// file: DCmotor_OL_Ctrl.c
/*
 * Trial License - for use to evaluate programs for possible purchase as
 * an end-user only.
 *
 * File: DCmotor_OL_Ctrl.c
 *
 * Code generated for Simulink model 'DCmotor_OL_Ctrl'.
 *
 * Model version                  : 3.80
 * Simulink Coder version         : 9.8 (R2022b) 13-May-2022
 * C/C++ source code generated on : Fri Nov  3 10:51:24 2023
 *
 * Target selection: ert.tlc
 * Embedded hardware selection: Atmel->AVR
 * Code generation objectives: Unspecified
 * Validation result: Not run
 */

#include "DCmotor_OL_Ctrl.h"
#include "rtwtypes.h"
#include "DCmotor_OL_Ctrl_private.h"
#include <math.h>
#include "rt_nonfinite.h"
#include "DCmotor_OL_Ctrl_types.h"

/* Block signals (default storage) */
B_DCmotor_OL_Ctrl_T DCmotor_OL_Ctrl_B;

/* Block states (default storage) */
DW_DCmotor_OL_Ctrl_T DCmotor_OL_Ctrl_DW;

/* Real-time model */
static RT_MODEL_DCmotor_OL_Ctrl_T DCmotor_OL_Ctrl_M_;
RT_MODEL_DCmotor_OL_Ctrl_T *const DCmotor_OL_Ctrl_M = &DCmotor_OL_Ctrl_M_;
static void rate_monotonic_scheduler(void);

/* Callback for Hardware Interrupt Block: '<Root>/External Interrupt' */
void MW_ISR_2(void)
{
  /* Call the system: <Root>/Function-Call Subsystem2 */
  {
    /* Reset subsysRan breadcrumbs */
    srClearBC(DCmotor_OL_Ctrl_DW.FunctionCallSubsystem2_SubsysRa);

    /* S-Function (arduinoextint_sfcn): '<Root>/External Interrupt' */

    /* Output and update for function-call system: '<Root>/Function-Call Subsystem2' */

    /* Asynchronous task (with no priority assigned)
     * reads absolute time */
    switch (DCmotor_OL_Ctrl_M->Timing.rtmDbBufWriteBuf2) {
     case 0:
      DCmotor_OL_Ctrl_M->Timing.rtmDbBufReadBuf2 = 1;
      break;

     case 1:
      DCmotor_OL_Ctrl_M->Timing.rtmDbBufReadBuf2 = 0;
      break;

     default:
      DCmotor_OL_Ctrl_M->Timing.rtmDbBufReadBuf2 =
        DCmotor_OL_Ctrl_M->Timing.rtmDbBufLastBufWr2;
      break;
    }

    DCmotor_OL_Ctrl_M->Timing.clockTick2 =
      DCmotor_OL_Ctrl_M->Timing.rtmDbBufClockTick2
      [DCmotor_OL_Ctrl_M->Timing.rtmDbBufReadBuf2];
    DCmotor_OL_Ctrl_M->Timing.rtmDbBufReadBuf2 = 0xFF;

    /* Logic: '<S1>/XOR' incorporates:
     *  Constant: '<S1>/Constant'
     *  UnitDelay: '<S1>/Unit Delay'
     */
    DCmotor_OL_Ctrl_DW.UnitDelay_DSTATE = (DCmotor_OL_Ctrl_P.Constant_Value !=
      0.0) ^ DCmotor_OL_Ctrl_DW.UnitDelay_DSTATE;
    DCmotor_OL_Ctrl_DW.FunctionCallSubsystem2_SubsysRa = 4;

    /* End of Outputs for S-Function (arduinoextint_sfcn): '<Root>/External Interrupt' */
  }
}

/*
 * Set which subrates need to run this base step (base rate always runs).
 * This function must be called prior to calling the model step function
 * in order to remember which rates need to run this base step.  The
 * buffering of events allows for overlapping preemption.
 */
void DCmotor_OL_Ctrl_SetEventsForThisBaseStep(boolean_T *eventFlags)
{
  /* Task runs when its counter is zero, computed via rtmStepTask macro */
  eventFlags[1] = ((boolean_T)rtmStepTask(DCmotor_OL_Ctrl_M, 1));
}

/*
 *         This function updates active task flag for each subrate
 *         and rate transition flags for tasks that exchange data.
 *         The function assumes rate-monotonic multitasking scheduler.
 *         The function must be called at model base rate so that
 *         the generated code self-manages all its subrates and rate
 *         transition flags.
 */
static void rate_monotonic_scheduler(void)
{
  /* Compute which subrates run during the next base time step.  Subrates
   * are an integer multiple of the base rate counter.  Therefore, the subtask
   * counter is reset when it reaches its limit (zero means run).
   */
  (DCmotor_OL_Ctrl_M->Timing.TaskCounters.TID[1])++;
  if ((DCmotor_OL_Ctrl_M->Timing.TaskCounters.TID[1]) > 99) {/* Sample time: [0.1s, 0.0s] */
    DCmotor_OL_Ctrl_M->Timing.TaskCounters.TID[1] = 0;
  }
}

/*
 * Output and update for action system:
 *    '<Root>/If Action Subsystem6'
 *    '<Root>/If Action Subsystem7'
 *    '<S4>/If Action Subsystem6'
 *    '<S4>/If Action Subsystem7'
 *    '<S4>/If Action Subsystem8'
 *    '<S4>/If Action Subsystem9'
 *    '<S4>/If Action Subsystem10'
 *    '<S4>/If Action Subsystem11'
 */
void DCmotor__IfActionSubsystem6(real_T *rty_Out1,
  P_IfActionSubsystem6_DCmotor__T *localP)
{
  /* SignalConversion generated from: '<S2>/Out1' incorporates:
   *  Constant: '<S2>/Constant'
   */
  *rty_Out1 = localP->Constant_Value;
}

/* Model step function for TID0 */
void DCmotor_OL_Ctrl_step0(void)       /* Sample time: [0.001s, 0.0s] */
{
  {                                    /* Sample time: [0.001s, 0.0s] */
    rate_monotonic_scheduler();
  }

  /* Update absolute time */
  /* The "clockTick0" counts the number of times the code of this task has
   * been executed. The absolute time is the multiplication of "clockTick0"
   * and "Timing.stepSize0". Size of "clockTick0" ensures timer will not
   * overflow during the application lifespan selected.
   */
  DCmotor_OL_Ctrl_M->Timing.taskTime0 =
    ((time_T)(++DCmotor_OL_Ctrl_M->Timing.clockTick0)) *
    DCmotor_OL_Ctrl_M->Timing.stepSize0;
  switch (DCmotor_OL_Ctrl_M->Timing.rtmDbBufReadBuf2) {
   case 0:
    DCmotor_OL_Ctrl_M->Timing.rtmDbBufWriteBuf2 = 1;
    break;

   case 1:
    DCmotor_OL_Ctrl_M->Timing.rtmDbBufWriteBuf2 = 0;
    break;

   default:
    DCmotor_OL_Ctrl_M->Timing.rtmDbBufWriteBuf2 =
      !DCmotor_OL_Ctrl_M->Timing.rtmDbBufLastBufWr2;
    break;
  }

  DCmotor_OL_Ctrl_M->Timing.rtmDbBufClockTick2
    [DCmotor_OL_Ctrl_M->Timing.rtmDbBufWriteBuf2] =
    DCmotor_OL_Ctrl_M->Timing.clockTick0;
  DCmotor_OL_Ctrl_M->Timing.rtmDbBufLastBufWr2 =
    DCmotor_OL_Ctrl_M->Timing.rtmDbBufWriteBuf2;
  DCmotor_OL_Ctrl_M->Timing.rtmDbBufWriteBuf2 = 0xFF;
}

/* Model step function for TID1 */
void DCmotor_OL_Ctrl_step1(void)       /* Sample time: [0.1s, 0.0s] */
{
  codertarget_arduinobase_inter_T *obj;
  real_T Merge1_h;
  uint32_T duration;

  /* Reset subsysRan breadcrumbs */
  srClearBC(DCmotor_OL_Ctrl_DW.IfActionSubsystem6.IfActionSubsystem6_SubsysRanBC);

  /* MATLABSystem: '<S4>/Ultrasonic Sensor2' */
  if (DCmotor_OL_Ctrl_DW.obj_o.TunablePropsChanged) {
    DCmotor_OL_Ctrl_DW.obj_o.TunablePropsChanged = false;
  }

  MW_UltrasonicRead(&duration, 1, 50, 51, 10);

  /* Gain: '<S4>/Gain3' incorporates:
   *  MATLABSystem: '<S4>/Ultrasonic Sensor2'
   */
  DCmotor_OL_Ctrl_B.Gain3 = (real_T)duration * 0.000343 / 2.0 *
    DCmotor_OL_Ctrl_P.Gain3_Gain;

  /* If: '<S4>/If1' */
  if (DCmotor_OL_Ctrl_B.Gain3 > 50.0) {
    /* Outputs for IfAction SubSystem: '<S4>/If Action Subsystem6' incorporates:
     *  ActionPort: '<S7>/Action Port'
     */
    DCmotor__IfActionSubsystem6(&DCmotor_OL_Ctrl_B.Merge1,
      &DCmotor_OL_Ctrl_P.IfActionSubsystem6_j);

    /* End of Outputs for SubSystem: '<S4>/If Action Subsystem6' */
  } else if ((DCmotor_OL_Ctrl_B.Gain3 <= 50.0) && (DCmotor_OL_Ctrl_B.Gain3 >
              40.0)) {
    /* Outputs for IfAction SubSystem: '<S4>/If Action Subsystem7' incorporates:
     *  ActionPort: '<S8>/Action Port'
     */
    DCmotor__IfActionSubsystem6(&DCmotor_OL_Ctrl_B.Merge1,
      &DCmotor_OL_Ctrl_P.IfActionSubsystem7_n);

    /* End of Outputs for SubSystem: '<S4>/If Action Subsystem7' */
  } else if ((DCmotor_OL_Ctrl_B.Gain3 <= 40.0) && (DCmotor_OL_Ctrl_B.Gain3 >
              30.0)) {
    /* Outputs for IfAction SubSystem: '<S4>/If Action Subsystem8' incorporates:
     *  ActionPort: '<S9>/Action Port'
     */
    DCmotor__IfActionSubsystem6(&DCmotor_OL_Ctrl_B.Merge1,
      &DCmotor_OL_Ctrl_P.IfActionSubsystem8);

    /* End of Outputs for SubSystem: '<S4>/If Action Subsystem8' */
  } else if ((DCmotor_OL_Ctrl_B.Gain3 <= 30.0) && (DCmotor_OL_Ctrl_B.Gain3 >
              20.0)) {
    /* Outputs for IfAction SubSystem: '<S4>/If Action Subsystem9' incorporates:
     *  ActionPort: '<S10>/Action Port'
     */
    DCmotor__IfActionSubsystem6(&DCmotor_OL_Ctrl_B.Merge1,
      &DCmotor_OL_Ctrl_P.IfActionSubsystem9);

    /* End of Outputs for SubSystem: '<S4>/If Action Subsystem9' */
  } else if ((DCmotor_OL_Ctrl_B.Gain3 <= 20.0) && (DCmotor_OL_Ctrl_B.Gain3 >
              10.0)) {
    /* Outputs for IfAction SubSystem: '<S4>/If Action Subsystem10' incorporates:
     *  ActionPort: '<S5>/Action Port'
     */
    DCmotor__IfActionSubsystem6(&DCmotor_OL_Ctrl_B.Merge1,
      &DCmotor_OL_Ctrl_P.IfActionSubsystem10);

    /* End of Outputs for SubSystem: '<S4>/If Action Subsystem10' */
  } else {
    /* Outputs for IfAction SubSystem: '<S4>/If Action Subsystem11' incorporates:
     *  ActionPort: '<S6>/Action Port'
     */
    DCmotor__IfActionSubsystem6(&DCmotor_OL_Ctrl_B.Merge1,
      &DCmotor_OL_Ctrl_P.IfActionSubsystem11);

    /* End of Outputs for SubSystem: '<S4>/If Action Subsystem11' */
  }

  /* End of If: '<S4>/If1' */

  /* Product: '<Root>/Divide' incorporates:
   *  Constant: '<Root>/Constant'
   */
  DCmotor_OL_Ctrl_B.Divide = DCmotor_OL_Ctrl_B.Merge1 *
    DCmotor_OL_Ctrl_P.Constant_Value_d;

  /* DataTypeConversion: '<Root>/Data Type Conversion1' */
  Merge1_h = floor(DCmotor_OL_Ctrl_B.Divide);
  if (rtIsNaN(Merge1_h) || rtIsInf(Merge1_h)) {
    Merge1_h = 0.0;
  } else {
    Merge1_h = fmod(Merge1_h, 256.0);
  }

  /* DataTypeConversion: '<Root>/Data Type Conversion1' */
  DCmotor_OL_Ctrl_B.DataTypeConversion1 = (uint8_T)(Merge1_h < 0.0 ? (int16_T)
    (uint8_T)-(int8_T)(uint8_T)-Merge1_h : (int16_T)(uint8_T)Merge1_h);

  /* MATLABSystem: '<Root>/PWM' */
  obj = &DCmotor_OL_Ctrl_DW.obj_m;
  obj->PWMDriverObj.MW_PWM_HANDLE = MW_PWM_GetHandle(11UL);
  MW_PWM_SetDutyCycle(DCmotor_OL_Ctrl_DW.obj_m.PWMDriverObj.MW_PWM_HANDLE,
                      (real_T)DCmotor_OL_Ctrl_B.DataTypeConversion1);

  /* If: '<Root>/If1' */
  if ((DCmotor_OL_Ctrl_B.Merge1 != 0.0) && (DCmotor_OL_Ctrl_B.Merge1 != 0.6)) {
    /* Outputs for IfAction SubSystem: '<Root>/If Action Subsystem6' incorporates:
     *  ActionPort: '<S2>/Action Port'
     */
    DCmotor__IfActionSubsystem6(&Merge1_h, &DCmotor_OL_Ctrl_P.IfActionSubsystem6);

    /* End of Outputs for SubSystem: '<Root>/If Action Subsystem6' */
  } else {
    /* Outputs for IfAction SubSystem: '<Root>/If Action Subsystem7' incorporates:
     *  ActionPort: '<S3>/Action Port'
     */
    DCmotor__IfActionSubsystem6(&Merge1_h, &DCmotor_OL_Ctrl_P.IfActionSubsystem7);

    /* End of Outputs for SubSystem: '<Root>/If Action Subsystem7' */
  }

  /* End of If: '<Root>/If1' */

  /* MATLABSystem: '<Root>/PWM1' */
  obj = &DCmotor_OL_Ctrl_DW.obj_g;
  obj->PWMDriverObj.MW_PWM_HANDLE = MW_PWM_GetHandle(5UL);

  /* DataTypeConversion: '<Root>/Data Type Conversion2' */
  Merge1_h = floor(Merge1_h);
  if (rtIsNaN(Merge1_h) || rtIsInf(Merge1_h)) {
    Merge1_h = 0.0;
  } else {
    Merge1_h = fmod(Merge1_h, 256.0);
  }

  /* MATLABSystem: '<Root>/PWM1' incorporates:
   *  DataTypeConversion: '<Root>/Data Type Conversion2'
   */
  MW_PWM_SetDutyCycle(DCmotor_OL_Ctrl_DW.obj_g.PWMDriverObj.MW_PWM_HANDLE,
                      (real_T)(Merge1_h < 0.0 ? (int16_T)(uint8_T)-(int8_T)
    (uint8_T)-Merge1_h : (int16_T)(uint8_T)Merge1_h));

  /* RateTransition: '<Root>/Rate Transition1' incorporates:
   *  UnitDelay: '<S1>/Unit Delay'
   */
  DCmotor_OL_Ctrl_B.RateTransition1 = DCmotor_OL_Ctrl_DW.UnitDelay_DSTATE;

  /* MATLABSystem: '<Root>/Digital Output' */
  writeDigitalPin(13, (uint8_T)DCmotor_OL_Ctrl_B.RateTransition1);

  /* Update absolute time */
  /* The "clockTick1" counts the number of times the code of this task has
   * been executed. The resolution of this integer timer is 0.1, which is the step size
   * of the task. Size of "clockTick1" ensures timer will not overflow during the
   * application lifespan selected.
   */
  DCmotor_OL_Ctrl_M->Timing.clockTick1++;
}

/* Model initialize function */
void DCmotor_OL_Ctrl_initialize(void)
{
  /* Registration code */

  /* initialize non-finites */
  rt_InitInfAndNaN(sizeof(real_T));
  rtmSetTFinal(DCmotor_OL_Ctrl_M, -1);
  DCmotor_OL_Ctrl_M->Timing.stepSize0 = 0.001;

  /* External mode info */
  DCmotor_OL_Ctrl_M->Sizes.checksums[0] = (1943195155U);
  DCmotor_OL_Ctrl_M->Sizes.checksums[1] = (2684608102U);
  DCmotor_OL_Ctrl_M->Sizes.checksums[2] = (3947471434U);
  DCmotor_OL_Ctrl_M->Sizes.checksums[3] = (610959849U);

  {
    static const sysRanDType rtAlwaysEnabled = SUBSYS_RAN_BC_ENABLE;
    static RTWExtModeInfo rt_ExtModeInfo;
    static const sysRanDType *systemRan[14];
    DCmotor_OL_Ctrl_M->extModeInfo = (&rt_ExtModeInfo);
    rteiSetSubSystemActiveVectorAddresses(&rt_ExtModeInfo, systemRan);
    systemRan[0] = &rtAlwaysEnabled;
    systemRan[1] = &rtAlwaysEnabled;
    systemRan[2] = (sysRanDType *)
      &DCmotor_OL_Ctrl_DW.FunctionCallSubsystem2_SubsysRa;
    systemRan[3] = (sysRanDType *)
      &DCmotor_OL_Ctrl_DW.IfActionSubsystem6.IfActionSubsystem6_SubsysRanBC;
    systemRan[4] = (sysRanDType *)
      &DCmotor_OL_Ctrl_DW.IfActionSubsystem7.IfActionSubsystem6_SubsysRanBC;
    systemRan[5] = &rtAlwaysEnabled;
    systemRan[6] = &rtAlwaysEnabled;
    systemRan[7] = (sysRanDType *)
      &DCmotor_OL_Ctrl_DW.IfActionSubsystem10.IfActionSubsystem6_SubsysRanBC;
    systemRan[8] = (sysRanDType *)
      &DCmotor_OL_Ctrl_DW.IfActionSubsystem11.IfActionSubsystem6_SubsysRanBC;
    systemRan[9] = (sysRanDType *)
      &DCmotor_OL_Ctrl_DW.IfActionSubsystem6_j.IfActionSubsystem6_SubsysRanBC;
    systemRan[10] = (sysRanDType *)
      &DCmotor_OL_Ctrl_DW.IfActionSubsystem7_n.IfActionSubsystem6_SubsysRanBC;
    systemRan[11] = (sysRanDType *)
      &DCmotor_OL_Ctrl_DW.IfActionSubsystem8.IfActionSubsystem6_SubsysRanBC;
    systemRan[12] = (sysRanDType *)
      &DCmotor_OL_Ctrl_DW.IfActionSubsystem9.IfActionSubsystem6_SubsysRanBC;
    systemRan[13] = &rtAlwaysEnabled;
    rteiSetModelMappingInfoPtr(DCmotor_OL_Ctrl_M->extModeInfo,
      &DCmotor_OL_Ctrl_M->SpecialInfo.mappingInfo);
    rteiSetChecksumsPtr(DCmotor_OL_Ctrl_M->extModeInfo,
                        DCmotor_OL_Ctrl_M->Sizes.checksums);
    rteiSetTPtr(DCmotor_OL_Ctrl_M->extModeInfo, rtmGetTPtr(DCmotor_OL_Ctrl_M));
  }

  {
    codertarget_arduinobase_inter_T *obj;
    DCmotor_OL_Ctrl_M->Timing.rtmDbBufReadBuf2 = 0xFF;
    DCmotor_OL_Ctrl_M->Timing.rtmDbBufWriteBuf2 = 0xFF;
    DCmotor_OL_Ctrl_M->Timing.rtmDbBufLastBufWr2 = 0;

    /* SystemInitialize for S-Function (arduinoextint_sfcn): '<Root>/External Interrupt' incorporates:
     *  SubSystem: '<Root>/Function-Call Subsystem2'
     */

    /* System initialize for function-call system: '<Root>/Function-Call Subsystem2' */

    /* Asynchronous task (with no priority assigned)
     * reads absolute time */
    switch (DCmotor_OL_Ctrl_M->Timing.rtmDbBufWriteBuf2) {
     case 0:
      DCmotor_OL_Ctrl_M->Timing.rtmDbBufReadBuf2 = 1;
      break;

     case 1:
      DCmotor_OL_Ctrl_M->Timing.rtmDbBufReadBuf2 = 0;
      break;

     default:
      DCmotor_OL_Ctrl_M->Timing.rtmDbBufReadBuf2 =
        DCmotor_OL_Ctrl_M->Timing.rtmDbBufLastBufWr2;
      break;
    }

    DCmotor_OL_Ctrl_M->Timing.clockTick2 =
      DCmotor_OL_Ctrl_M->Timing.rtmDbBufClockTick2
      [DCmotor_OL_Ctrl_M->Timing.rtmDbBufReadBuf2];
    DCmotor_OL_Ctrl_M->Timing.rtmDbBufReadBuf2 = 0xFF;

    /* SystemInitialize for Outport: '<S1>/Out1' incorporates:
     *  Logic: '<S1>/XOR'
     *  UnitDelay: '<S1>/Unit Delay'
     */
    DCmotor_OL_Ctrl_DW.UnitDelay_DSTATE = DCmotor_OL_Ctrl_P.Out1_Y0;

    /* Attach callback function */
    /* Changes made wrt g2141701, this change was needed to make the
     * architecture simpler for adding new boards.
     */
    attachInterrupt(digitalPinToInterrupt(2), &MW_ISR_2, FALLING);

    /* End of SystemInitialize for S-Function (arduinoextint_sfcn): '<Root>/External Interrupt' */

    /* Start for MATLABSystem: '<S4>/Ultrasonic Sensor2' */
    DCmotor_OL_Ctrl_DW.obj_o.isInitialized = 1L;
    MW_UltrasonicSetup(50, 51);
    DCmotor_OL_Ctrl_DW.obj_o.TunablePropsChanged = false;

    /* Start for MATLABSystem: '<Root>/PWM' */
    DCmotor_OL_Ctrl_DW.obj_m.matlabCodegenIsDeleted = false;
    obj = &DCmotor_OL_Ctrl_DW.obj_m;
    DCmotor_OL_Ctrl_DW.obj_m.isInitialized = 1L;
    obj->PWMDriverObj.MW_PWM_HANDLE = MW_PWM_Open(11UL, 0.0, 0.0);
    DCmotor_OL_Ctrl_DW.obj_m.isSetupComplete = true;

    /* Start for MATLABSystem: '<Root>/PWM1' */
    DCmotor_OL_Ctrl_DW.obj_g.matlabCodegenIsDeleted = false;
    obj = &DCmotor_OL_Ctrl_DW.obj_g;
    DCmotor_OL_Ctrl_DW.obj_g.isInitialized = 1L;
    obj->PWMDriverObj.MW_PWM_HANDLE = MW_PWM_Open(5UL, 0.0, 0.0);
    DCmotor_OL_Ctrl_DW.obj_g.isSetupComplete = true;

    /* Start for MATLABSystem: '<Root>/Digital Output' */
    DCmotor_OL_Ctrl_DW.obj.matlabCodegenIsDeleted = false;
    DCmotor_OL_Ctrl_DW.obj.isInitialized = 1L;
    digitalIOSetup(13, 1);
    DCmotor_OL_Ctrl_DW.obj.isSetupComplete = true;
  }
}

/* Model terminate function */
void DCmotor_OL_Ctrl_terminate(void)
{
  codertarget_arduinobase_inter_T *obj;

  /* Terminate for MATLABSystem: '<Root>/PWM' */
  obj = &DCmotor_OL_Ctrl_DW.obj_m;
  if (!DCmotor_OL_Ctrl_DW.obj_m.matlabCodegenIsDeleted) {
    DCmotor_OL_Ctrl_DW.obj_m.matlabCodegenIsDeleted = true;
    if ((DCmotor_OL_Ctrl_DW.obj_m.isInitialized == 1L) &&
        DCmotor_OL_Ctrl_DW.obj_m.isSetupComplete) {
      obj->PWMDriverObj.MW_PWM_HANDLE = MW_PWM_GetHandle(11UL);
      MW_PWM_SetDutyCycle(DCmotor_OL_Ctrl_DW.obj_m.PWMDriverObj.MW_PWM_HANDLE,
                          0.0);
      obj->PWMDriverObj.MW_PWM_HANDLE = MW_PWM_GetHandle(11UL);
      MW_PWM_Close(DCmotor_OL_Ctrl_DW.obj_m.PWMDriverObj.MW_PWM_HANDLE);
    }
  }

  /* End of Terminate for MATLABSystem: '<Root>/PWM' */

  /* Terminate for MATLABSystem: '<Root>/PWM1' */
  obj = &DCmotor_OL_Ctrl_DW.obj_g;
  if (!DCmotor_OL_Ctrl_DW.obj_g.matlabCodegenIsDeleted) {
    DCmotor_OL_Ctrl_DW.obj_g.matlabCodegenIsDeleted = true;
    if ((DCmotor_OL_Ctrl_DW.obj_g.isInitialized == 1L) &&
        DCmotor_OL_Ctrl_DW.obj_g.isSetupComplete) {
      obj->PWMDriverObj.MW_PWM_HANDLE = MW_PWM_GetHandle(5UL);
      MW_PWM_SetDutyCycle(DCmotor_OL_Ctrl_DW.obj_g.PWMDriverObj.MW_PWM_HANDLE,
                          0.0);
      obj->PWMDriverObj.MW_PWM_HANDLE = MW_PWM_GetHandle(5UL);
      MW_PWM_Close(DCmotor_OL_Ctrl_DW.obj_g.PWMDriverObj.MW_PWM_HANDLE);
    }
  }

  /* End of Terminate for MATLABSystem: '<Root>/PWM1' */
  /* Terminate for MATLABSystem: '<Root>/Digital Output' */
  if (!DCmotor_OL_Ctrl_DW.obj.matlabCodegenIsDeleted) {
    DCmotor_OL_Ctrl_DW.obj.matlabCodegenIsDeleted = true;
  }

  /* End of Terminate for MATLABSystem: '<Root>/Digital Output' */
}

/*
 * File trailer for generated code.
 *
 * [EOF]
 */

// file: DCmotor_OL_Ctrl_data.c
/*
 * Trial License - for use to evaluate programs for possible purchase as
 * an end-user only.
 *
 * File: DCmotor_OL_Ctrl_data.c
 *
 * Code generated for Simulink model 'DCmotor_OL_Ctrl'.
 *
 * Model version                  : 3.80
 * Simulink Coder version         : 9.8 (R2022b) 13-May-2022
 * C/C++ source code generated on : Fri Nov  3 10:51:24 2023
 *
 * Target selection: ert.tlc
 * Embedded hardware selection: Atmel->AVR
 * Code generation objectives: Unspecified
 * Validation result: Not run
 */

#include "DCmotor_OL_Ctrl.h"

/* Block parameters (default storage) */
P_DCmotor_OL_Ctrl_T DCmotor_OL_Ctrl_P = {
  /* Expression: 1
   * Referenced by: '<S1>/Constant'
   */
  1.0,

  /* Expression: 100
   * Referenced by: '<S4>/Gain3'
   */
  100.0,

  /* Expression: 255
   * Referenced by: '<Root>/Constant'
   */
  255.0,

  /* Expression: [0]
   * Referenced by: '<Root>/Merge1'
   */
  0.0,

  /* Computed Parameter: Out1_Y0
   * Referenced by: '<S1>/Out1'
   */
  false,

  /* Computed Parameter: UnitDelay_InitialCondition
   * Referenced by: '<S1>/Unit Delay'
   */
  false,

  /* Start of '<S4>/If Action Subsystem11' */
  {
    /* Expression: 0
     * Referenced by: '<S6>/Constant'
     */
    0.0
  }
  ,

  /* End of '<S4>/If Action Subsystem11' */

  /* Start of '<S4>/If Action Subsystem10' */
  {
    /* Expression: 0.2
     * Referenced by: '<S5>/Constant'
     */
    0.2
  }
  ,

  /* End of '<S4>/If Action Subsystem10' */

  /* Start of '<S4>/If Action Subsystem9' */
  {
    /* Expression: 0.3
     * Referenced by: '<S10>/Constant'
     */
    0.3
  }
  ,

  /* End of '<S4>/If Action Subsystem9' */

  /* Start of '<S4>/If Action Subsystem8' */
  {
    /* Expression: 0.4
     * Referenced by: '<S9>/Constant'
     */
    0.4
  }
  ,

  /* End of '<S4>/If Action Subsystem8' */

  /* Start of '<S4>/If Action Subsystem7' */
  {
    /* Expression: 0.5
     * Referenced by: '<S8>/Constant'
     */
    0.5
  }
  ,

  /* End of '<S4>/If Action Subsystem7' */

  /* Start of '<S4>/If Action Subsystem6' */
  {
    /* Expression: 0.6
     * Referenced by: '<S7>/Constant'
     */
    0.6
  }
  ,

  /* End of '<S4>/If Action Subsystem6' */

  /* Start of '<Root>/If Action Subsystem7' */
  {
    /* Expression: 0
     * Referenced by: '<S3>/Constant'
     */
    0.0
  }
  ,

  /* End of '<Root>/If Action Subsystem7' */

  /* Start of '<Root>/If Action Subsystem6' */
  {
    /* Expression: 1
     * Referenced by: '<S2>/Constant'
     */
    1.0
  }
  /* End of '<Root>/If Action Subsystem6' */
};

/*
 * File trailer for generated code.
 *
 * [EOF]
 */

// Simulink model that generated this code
simulink model "DCmotor_OL_Ctrl"  (R2022b)
settings: Solver=ode4  StartTime=0.0  StopTime=inf  FixedStep=0.001  RelTol=1e-3  EnableMultiTasking=on
libraries: arduinolib x5, arduinosensorlib x2

== system DCmotor_OL_Ctrl ==
  note: Speed Control
  note: Ultra Sensor
  note: Direction Control
  Analog Input : arduinolib/Analog Input  Commented=on  pinNumber=0  ReadResultsOnly=off  ConversionTriggerSource=Software  ExternalTriggerType=uint32( 0 )  OutputDataType=uint16  EnableConversionCompleteNotify=off  EnableOuputStatus=off  SampleTime=-1  blockPlatform=arduino
  Constant : Constant  Value=255
  Data Type Conversion : DataTypeConversion  Commented=on  OutDataTypeStr=uint8  SaturateOnIntegerOverflow=off  RndMeth=Floor
  Data Type Conversion1 : DataTypeConversion  OutDataTypeStr=uint8  SaturateOnIntegerOverflow=off  RndMeth=Floor
  Data Type Conversion2 : DataTypeConversion  OutDataTypeStr=uint8  SaturateOnIntegerOverflow=off  RndMeth=Floor
  Digital Output : arduinolib/Digital Output  Commented=on  pinNumber=13  Direction=output  blockPlatform=arduino
  Display Status1 : Display  Commented=on
  Display1 : Display
  Display2 : Display
  Display3 : Display  Commented=on
  Divide : Product  Inputs=**
  External Interrupt : arduinolib/External Interrupt  Commented=on  Pin=2  PullUp=off  Mode=FALLING  InterruptSimulationInput=off
  Function-Call Subsystem : Subsystem  Commented=on  TreatAsAtomicUnit=on
  Function-Call Subsystem2 : Subsystem  Commented=on  TreatAsAtomicUnit=on
  Gain1 : Gain  Commented=on  Gain=0.25
  Gain2 : Gain  Commented=on  Gain=100
  If : If  Commented=on  IfExpression=u1 > 50  ElseIfExpressions=u1 > 40, u1 > 30, u1 > 20, u1 > 10
  If Action Subsystem : Subsystem  Commented=on  TreatAsAtomicUnit=on
  If Action Subsystem1 : Subsystem  Commented=on  TreatAsAtomicUnit=on
  If Action Subsystem2 : Subsystem  Commented=on  TreatAsAtomicUnit=on
  If Action Subsystem3 : Subsystem  Commented=on  TreatAsAtomicUnit=on
  If Action Subsystem4 : Subsystem  Commented=on  TreatAsAtomicUnit=on
  If Action Subsystem5 : Subsystem  Commented=on  TreatAsAtomicUnit=on
  If Action Subsystem6 : Subsystem  TreatAsAtomicUnit=on
  If Action Subsystem7 : Subsystem  TreatAsAtomicUnit=on
  If1 : If  IfExpression=u1 ~= 0 & u1 ~= 0.6
  Merge : Merge  Commented=on  Inputs=6
  Merge1 : Merge  InitialOutput=[0]
  PWM : arduinolib/PWM  pinNumber=11  frequencyType=Default  desiredFrequency=490.2  achievableFrequency=490.2
  PWM1 : arduinolib/PWM  pinNumber=5  frequencyType=Default  desiredFrequency=490.2  achievableFrequency=490.2
  Rate Transition1 : RateTransition  Commented=on  Deterministic=off
  Subsystem : Subsystem
  Ultrasonic Sensor1 : arduinosensorlib/Ultrasonic Sensor  Commented=on  NumSignalPins=2  TrigPin=50  EchoPin=51  SignalPin=3  SampleTime_=0.1  blockPlatform=ARDUINO
  Scope : Scope
  wires:
  Analog Input/1 -> Gain1/1
  Gain1/1 -> Data Type Conversion/1
  Constant/1 -> Divide/2
  Data Type Conversion1/1 -> PWM/1, Display2/1
  Gain2/1 -> Display3/1, If/1
  Ultrasonic Sensor1/1 -> Gain2/1
  If/2 -> If Action Subsystem1/Action
  If/1 -> If Action Subsystem/Action
  If/3 -> If Action Subsystem2/Action
  If/4 -> If Action Subsystem3/Action
  If/5 -> If Action Subsystem4/Action
  If/6 -> If Action Subsystem5/Action
  If Action Subsystem/1(Out1) -> Merge/1
  If Action Subsystem1/1(Out1) -> Merge/2
  If Action Subsystem2/1(Out1) -> Merge/3
  If Action Subsystem3/1(Out1) -> Merge/4
  If Action Subsystem4/1(Out1) -> Merge/5
  If Action Subsystem5/1(Out1) -> Merge/6
  Divide/1 -> Display1/1, Data Type Conversion1/1
  Function-Call Subsystem2/1(Out1) -> Rate Transition1/1
  Rate Transition1/1 -> Display Status1/1, Digital Output/1
  External Interrupt/1 -> Function-Call Subsystem2/Trigger
  Subsystem/1(Output) -> Divide/1, If1/1
  Data Type Conversion2/1 -> PWM1/1
  If Action Subsystem6/1(Out1) -> Merge1/1
  If Action Subsystem7/1(Out1) -> Merge1/2
  If1/1 -> If Action Subsystem6/Action
  If1/2 -> If Action Subsystem7/Action
  Merge1/1 -> Data Type Conversion2/1

== system DCmotor_OL_Ctrl/Function-Call Subsystem ==
  function : TriggerPort  TriggerType=function-call  VariantControl=(inherit)
  Constant : Constant
  MATLAB Function : MATLAB Function  TreatAsAtomicUnit=on
  Sum : Sum  Inputs=|++
  Unit Delay : UnitDelay  SampleTime=-1  HasFrameUpgradeWarning=on
  Out1 : Outport
  wires:
  Constant/1 -> Sum/1
  Unit Delay/1 -> Sum/2
  Sum/1 -> Unit Delay/1, MATLAB Function/1(u)
  MATLAB Function/1(y) -> Out1/1

== system DCmotor_OL_Ctrl/Function-Call Subsystem2 ==
  function : TriggerPort  TriggerType=function-call  VariantControl=(inherit)
  Constant : Constant
  Unit Delay : UnitDelay  SampleTime=-1  HasFrameUpgradeWarning=on
  XOR : Logic  Operator=XOR  IconShape=distinctive  AllPortsSameDT=off  OutDataTypeStr=boolean
  Out1 : Outport
  wires:
  Constant/1 -> XOR/1
  Unit Delay/1 -> XOR/2
  XOR/1 -> Unit Delay/1, Out1/1

== system DCmotor_OL_Ctrl/If Action Subsystem ==
  Action Port : ActionPort  ActionPortLabel=if(u1 > 50)
  Constant : Constant
  Out1 : Outport
  wires:
  Constant/1 -> Out1/1

== system DCmotor_OL_Ctrl/If Action Subsystem1 ==
  Action Port : ActionPort  ActionPortLabel=elseif(u1 > 40)
  Constant : Constant  Value=10
  Out1 : Outport
  wires:
  Constant/1 -> Out1/1

== system DCmotor_OL_Ctrl/If Action Subsystem2 ==
  Action Port : ActionPort  ActionPortLabel=elseif( u1 > 30)
  Constant : Constant  Value=10
  Out1 : Outport
  wires:
  Constant/1 -> Out1/1

== system DCmotor_OL_Ctrl/If Action Subsystem3 ==
  Action Port : ActionPort  ActionPortLabel=elseif( u1 > 20)
  Constant : Constant  Value=10
  Out1 : Outport
  wires:
  Constant/1 -> Out1/1

== system DCmotor_OL_Ctrl/If Action Subsystem4 ==
  Action Port : ActionPort  ActionPortLabel=elseif( u1 > 10)
  Constant : Constant  Value=10
  Out1 : Outport
  wires:
  Constant/1 -> Out1/1

== system DCmotor_OL_Ctrl/If Action Subsystem5 ==
  Action Port : ActionPort  ActionPortLabel=else
  Constant : Constant  Value=0
  Out1 : Outport
  wires:
  Constant/1 -> Out1/1

== system DCmotor_OL_Ctrl/If Action Subsystem6 ==
  Action Port : ActionPort  ActionPortLabel=if(u1 ~= 0 & u1 ~= 0.6)
  Constant : Constant  Value=10
  Out1 : Outport
  wires:
  Constant/1 -> Out1/1

== system DCmotor_OL_Ctrl/If Action Subsystem7 ==
  Action Port : ActionPort  ActionPortLabel=else
  Constant : Constant  Value=0
  Out1 : Outport
  wires:
  Constant/1 -> Out1/1

== system DCmotor_OL_Ctrl/Subsystem ==
  note: Ultra Sensor
  Display1 : Display
  Display4 : Display
  Gain3 : Gain  Gain=100
  If Action Subsystem10 : Subsystem  TreatAsAtomicUnit=on
  If Action Subsystem11 : Subsystem  TreatAsAtomicUnit=on
  If Action Subsystem6 : Subsystem  TreatAsAtomicUnit=on
  If Action Subsystem7 : Subsystem  TreatAsAtomicUnit=on
  If Action Subsystem8 : Subsystem  TreatAsAtomicUnit=on
  If Action Subsystem9 : Subsystem  TreatAsAtomicUnit=on
  If1 : If  IfExpression=u1 > 50  ElseIfExpressions=50>= u1 & u1> 40, 40>=u1 & u1>30, 30>= u1 & u1 > 20, 20>= u1 & u1 > 10
  Merge1 : Merge  Inputs=6
  Ultrasonic Sensor2 : arduinosensorlib/Ultrasonic Sensor  NumSignalPins=2  TrigPin=50  EchoPin=51  SignalPin=3  SampleTime_=0.1  blockPlatform=ARDUINO
  Output : Outport
  wires:
  Gain3/1 -> If1/1, Display4/1
  Ultrasonic Sensor2/1 -> Gain3/1
  If Action Subsystem9/1(Out1) -> Merge1/4
  If Action Subsystem11/1(Out1) -> Merge1/6
  If Action Subsystem8/1(Out1) -> Merge1/3
  If Action Subsystem7/1(Out1) -> Merge1/2
  If Action Subsystem6/1(Out1) -> Merge1/1
  If Action Subsystem10/1(Out1) -> Merge1/5
  If1/1 -> If Action Subsystem6/Action
  If1/2 -> If Action Subsystem7/Action
  If1/3 -> If Action Subsystem8/Action
  If1/4 -> If Action Subsystem9/Action
  If1/5 -> If Action Subsystem10/Action
  If1/6 -> If Action Subsystem11/Action
  Merge1/1 -> Display1/1, Output/1

== system DCmotor_OL_Ctrl/Subsystem/If Action Subsystem10 ==
  Action Port : ActionPort  ActionPortLabel=elseif( 20>= u1 & u1 > 10)
  Constant : Constant  Value=0.2
  Out1 : Outport
  wires:
  Constant/1 -> Out1/1

== system DCmotor_OL_Ctrl/Subsystem/If Action Subsystem11 ==
  Action Port : ActionPort  ActionPortLabel=else
  Constant : Constant  Value=0
  Out1 : Outport
  wires:
  Constant/1 -> Out1/1

== system DCmotor_OL_Ctrl/Subsystem/If Action Subsystem6 ==
  Action Port : ActionPort  ActionPortLabel=if(u1 > 50)
  Constant : Constant  Value=0.6
  Out1 : Outport
  wires:
  Constant/1 -> Out1/1

== system DCmotor_OL_Ctrl/Subsystem/If Action Subsystem7 ==
  Action Port : ActionPort  ActionPortLabel=elseif(50>= u1 & u1> 40)
  Constant : Constant  Value=0.5
  Out1 : Outport
  wires:
  Constant/1 -> Out1/1

== system DCmotor_OL_Ctrl/Subsystem/If Action Subsystem8 ==
  Action Port : ActionPort  ActionPortLabel=elseif( 40>=u1 & u1>30)
  Constant : Constant  Value=0.4
  Out1 : Outport
  wires:
  Constant/1 -> Out1/1

== system DCmotor_OL_Ctrl/Subsystem/If Action Subsystem9 ==
  Action Port : ActionPort  ActionPortLabel=elseif( 30>= u1 & u1 > 20)
  Constant : Constant  Value=0.3
  Out1 : Outport
  wires:
  Constant/1 -> Out1/1

== matlab function DCmotor_OL_Ctrl/Function-Call Subsystem/MATLAB Function ==
function y = fcn(u)
 rem = mod(u,2);
 if rem == 0
     y=0;
 else
     y=1;
 end

 if u > 100
     u = 1;
 end
